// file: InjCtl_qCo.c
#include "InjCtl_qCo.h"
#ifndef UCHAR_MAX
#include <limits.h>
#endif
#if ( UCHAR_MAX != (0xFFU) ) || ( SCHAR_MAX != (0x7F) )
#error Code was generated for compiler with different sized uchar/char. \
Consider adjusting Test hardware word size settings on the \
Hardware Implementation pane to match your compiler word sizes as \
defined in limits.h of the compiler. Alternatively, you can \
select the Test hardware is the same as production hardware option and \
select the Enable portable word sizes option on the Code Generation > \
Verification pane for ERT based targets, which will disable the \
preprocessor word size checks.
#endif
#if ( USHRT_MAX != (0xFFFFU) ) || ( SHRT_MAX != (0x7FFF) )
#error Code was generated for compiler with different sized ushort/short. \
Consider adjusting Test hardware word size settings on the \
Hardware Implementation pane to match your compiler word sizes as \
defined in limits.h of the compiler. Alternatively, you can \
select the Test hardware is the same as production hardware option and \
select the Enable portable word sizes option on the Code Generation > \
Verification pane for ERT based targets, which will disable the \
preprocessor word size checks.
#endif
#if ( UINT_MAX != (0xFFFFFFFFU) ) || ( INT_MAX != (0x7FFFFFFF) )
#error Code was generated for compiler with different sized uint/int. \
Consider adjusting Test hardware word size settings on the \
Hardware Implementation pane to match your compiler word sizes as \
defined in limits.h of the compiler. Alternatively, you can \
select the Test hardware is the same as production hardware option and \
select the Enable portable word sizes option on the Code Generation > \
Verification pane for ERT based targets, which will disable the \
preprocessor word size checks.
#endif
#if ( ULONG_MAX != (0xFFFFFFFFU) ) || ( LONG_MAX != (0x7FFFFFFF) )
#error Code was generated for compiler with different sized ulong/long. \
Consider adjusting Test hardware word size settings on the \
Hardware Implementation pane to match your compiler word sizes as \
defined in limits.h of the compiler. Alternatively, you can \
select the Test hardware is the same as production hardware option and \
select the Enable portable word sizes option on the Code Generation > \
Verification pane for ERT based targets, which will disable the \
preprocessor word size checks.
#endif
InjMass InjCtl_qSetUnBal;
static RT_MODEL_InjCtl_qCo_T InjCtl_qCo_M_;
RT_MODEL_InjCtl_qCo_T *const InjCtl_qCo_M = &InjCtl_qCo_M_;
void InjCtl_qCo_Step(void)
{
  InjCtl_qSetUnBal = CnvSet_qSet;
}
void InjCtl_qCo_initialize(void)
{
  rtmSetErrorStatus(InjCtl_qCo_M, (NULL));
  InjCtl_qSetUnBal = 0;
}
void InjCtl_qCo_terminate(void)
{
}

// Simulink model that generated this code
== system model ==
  InjCtl_qCo_Step : Inport
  CnvSet_qSet : Inport
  InjCtl_qSetUnBal : Outport  <- 1: InjCtl_qCo
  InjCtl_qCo : Subsystem  <- 1: CnvSet_qSet, Trigger: InjCtl_qCo_Step
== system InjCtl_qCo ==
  Inport#1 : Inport
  TriggerPort#1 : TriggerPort  TriggerType=function-call
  Outport#1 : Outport  <- 1: SignalConversion#1
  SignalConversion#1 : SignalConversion  <- 1: Inport#1
